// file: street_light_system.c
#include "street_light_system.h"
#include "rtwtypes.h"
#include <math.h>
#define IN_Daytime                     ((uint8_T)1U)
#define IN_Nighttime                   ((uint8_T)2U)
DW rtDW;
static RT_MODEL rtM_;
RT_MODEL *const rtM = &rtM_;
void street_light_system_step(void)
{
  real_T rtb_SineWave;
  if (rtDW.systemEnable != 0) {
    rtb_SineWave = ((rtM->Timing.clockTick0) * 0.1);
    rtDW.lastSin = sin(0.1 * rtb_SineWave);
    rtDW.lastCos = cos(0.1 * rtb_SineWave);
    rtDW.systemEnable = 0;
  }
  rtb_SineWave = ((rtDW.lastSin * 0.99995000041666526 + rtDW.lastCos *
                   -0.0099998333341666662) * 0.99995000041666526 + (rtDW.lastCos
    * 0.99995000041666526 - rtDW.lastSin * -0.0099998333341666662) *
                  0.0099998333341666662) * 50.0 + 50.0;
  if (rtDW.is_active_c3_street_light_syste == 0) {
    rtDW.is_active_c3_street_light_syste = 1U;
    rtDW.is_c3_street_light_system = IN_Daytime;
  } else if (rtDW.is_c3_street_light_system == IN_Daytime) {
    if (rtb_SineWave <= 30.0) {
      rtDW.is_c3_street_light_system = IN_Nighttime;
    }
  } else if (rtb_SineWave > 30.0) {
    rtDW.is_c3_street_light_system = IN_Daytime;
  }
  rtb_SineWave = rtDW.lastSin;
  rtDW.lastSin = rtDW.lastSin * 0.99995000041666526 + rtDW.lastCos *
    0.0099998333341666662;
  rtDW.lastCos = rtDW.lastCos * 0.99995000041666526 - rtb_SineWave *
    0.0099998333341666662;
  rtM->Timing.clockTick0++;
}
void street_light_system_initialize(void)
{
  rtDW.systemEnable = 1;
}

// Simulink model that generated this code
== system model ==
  Stateflowchart#1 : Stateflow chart  <- 1: SineWave
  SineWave : Sin  Amplitude=50  Bias=50  Frequency=0.1
== stateflow chart Stateflowchart#1 ==
  state Daytime
    light = 0;
  state Nighttime
    light = 1;
  (default) -> Daytime
  Nighttime -> Daytime : [light_level >  30]
  Daytime -> Nighttime : [light_level <= 30]
  data: light_level input double; light output double
